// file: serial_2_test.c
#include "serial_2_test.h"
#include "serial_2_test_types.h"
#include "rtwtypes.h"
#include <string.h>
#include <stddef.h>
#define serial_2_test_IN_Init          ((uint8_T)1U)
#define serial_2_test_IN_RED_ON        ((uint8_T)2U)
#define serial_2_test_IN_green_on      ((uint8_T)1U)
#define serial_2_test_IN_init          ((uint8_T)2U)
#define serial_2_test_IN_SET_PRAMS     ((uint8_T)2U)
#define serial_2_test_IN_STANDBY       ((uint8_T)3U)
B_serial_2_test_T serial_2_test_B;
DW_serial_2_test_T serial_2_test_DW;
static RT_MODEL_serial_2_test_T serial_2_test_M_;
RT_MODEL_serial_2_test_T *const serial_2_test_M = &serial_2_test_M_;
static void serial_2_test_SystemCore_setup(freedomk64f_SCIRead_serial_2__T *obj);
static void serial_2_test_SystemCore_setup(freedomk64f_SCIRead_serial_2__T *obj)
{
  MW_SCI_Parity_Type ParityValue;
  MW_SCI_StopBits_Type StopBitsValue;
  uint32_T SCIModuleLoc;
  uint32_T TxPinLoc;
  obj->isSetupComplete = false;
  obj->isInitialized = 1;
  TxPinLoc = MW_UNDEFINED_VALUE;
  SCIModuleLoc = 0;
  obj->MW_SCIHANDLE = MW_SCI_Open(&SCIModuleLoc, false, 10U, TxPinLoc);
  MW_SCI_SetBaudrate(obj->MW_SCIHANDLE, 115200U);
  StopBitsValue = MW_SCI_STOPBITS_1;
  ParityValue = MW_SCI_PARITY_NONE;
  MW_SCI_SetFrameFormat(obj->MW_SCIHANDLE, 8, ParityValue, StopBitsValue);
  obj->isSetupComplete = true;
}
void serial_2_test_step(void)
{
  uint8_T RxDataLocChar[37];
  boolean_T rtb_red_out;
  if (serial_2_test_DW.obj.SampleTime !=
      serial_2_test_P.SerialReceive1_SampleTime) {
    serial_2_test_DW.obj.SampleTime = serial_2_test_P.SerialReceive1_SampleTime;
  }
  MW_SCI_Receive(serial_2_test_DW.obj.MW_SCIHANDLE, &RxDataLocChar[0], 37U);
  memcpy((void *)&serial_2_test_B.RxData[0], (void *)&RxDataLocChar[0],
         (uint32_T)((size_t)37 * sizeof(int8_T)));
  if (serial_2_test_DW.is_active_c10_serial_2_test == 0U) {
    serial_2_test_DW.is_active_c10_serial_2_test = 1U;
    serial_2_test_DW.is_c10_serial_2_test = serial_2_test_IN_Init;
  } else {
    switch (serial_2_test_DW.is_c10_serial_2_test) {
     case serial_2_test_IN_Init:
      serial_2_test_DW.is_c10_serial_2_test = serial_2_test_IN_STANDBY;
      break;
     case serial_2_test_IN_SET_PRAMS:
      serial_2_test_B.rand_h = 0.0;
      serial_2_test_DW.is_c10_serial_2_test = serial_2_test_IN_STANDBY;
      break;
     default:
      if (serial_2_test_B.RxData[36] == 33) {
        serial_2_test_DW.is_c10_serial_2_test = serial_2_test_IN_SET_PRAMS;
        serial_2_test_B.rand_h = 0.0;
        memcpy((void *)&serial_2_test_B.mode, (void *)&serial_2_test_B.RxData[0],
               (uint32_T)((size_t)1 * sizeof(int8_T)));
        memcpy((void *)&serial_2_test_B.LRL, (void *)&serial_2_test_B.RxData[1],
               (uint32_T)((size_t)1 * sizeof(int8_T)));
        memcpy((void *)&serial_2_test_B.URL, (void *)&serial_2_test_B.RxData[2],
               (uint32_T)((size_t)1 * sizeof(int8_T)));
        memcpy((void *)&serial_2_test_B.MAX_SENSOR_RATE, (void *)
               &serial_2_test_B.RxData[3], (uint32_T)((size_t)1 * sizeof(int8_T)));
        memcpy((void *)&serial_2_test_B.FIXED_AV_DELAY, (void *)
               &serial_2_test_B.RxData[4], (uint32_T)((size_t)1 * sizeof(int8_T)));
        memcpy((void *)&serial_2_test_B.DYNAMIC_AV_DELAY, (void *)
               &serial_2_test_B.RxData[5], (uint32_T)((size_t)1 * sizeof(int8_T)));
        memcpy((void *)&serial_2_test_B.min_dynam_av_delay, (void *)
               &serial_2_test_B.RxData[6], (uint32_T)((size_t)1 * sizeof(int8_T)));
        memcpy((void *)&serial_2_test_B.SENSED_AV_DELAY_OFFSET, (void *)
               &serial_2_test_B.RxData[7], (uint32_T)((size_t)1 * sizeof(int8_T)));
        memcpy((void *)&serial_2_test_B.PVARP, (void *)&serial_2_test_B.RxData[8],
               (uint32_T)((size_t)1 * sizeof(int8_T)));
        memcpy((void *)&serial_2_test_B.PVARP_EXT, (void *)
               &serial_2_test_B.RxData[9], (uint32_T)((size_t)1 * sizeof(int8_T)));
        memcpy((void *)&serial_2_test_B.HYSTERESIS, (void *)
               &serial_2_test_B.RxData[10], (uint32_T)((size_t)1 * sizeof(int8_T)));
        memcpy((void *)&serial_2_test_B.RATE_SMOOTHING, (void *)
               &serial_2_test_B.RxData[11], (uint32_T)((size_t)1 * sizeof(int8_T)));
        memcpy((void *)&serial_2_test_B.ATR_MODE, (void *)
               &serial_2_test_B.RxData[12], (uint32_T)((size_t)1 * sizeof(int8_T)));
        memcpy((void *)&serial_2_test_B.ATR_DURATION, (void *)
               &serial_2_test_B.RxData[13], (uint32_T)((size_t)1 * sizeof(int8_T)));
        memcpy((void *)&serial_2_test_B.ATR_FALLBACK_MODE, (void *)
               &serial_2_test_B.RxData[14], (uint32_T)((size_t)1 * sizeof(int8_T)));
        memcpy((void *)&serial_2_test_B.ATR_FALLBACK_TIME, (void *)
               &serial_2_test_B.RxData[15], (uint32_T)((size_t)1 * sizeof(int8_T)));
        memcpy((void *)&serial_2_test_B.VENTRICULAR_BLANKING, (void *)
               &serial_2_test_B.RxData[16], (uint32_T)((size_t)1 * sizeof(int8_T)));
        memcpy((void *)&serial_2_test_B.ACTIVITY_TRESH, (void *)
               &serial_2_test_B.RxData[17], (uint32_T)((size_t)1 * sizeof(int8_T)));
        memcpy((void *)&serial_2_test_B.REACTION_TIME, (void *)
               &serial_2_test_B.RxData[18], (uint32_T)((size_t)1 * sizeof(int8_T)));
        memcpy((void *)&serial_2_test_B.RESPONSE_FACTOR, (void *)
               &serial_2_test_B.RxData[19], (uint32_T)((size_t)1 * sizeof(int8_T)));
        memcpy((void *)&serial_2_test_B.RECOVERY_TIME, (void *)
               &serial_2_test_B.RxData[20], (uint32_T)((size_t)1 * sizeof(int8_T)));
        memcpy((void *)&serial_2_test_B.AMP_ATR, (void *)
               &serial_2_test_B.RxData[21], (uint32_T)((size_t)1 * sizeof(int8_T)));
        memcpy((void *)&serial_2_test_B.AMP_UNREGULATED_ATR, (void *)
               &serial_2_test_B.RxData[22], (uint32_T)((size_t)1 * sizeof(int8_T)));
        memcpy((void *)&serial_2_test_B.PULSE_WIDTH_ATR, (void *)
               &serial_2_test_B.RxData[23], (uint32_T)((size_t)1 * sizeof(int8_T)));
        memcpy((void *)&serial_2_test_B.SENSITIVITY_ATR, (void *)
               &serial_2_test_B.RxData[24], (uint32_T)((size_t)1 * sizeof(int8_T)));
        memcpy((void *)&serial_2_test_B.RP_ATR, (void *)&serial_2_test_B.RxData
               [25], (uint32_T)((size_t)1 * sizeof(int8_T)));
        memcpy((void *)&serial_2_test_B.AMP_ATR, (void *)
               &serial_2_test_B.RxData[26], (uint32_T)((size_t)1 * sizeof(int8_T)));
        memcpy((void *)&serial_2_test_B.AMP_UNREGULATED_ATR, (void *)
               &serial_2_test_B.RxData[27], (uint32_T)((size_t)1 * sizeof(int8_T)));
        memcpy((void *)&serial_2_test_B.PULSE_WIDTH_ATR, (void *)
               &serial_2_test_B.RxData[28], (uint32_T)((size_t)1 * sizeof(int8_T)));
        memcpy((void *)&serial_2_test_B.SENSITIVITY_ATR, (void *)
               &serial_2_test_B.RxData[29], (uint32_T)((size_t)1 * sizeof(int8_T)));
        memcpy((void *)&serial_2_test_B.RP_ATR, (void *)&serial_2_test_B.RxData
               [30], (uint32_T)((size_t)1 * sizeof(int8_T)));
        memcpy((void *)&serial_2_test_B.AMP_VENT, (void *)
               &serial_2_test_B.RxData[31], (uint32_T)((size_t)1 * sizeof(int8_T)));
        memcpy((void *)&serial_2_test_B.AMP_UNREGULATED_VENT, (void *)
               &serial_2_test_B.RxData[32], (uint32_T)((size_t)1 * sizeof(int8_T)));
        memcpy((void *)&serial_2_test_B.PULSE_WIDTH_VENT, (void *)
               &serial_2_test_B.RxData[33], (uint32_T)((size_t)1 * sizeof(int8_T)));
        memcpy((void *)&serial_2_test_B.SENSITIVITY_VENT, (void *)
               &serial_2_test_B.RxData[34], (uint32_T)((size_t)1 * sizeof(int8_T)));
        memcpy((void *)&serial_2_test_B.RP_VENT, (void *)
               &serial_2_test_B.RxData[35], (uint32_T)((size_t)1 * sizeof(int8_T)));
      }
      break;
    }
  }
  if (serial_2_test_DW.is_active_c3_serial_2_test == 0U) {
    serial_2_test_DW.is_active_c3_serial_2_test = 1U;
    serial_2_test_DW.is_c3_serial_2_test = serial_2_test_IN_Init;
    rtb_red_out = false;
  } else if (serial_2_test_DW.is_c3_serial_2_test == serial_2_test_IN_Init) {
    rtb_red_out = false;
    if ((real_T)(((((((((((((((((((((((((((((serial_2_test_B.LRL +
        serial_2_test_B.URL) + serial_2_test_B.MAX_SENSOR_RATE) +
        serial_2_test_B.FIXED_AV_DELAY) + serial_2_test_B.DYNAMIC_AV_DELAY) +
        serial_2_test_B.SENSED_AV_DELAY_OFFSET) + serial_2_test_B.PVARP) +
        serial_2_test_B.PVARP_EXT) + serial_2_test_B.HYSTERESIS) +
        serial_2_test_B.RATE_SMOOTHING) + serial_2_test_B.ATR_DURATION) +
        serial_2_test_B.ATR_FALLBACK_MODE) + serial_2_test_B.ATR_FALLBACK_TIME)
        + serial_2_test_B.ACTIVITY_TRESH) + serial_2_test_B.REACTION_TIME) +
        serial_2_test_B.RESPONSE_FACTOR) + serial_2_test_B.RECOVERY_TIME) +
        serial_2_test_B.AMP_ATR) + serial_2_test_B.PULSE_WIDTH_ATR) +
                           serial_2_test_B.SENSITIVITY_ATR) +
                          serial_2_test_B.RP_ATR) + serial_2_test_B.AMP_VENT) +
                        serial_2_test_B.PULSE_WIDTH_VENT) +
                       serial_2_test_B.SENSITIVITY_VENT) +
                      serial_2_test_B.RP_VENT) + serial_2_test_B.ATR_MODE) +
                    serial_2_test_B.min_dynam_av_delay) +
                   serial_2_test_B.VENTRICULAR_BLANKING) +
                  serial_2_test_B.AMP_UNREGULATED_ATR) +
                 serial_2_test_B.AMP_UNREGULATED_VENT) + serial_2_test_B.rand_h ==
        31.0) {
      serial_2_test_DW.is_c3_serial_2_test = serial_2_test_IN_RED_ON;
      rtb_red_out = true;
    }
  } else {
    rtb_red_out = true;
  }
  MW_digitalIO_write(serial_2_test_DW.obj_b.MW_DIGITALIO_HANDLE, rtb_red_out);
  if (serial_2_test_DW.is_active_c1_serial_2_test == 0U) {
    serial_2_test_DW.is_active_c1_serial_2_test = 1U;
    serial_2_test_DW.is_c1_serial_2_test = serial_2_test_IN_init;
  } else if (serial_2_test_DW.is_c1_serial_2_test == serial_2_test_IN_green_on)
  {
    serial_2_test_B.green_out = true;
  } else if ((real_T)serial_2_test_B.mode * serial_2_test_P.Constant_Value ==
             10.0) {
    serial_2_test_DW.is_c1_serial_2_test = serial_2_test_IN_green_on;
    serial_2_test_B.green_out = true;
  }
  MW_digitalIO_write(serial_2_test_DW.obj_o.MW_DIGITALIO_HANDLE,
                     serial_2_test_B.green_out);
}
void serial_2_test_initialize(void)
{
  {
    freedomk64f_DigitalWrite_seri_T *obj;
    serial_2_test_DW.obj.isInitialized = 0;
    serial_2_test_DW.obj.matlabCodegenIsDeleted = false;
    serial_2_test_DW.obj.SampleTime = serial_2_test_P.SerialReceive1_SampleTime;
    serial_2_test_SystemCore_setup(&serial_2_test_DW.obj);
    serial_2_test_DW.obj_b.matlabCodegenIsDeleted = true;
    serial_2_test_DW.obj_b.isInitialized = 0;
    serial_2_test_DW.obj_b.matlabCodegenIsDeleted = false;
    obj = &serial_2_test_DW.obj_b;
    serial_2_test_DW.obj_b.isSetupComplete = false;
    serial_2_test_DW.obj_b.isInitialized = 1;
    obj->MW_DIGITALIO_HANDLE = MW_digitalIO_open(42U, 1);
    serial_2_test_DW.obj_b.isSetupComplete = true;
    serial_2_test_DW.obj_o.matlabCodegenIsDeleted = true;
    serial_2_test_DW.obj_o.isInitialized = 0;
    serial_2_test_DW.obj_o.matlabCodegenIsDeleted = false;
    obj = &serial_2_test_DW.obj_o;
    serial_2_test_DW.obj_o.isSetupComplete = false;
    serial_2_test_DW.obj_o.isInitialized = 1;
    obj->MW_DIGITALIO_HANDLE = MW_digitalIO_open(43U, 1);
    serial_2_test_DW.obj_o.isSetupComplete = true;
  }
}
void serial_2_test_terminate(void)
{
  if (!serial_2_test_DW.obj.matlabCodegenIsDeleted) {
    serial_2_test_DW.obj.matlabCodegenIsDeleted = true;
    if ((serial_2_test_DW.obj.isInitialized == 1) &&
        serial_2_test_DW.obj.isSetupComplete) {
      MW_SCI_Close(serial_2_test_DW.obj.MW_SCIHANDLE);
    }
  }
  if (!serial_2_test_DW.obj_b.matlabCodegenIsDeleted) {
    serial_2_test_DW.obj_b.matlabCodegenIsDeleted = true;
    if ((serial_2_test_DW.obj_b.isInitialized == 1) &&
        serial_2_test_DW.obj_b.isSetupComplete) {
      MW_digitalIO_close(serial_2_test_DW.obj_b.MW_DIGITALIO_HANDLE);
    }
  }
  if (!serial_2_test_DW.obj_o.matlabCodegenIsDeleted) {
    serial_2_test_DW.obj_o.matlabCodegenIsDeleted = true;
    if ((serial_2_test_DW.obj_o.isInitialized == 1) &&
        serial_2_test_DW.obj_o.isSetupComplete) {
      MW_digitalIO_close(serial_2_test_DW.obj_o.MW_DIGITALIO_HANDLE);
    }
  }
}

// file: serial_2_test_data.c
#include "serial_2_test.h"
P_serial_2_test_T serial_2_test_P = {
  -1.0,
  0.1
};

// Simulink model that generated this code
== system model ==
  DigitalWrite : frdmk64flib/Digital Write  <- 1: Stateflowchart#1
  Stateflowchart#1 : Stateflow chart  <- 1: Sum#1
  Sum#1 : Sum  Inputs=++++++++++++++++++++++++++++++++  <- 1: Stateflowchart#2, 2: Stateflowchart#2/2, 3: Stateflowchart#2/3, 4: Stateflowchart#2/4, 5: Stateflowchart#2/5, 6: Stateflowchart#2/6, 7: Stateflowchart#2/7, 8: Stateflowchart#2/8, 9: Stateflowchart#2/9, 10: Stateflowchart#2/10, 11: Stateflowchart#2/11, 12: Stateflowchart#2/12, 13: Stateflowchart#2/13, 14: Stateflowchart#2/14, 15: Stateflowchart#2/15, 16: Stateflowchart#2/16, 17: Stateflowchart#2/17, 18: Stateflowchart#2/18, 19: Stateflowchart#2/19, 20: Stateflowchart#2/20, 21: Stateflowchart#2/21, 22: Stateflowchart#2/22, 23: Stateflowchart#2/23, 24: Stateflowchart#2/24, 25: Stateflowchart#2/25, 26: Stateflowchart#2/26, 27: Stateflowchart#2/27, 28: Stateflowchart#2/28, 29: Stateflowchart#2/29, 30: Stateflowchart#2/30, 31: Stateflowchart#2/31
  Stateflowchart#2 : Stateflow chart  <- 1: SerialReceive1
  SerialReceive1 : frdmk64flib/Serial Receive
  DigitalWrite#1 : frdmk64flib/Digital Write  <- 1: Stateflowchart#3
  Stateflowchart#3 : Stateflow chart  <- 1: Product#1
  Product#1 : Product  <- 1: Stateflowchart#2/32, 2: Constant
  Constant : Constant  Value=1/10
== stateflow chart Stateflowchart#2 ==
  state SET_PRAMS
    entry:
    rand = 0;
    mode = typecast(rxdata(1),'int8');
    LRL =  typecast(rxdata(2),'int8');
    URL = typecast(rxdata(3),'int8');
    MAX_SENSOR_RATE =  typecast(rxdata(4),'int8');
    FIXED_AV_DELAY =  typecast(rxdata(5),'int8');
    DYNAMIC_AV_DELAY =  typecast(rxdata(6),'int8');
    min_dynam_av_delay = typecast(rxdata(7),'int8');
    SENSED_AV_DELAY_OFFSET =typecast(rxdata(8),'int8');
    PVARP = typecast(rxdata(9),'int8');
    PVARP_EXT = typecast(rxdata(10),'int8');
    HYSTERESIS = typecast(rxdata(11),'int8');
    RATE_SMOOTHING = typecast(rxdata(12),'int8');
    ATR_MODE = typecast(rxdata(13),'int8');
    ATR_DURATION = typecast(rxdata(14),'int8');
    ATR_FALLBACK_MODE =typecast(rxdata(15),'int8');
    ATR_FALLBACK_TIME = typecast(rxdata(16),'int8');
    VENTRICULAR_BLANKING =typecast(rxdata(17),'int8');
    ACTIVITY_TRESH =typecast(rxdata(18),'int8');
    REACTION_TIME = typecast(rxdata(19),'int8');
    RESPONSE_FACTOR =typecast(rxdata(20),'int8');
    RECOVERY_TIME = typecast(rxdata(21),'int8');
    AMP_ATR =typecast(rxdata(22),'int8');
    AMP_UNREGULATED_ATR =typecast(rxdata(23),'int8');
    PULSE_WIDTH_ATR=typecast(rxdata(24),'int8');
    SENSITIVITY_ATR =typecast(rxdata(25),'int8');
    RP_ATR = typecast(rxdata(26),'int8');
    AMP_ATR =typecast(rxdata(27),'int8');
    AMP_UNREGULATED_ATR =typecast(rxdata(28),'int8');
    PULSE_WIDTH_ATR=typecast(rxdata(29),'int8');
    SENSITIVITY_ATR =typecast(rxdata(30),'int8');
    RP_ATR = typecast(rxdata(31),'int8');
    AMP_VENT =typecast(rxdata(32),'int8');
    AMP_UNREGULATED_VENT =typecast(rxdata(33),'int8');
    PULSE_WIDTH_VENT=typecast(rxdata(34),'int8');
    SENSITIVITY_VENT = typecast(rxdata(35),'int8');
    RP_VENT =typecast(rxdata(36),'int8');
  state Init
    entry:
  state STANDBY
  (default) -> Init
  Init -> STANDBY
  STANDBY -> SET_PRAMS : [rxdata(37) == hex2dec('21')]
  SET_PRAMS -> STANDBY
  data: rxdata input; LRL output size=1; URL output size=1; MAX_SENSOR_RATE output size=1; FIXED_AV_DELAY output size=1; DYNAMIC_AV_DELAY output size=1; SENSED_AV_DELAY_OFFSET output size=1; PVARP output size=1; PVARP_EXT output size=1; HYSTERESIS output size=1; RATE_SMOOTHING output size=1; ATR_DURATION output size=1; ATR_FALLBACK_MODE output size=1; ATR_FALLBACK_TIME output size=1; ACTIVITY_TRESH output size=1; REACTION_TIME output size=1; RESPONSE_FACTOR output size=1; RECOVERY_TIME output size=1; AMP_ATR output size=1; PULSE_WIDTH_ATR output size=1; SENSITIVITY_ATR output size=1; RP_ATR output size=1; AMP_VENT output size=1; PULSE_WIDTH_VENT output size=1; SENSITIVITY_VENT output size=1; RP_VENT output size=1; ATR_MODE output size=1; min_dynam_av_delay output size=1; VENTRICULAR_BLANKING output size=1; AMP_UNREGULATED_ATR output size=1; AMP_UNREGULATED_VENT output size=1; rand output size=1; mode output size=1

== stateflow chart Stateflowchart#3 ==
  state green_on
    entry:
    green_out = true;
  state init
    entry:
  (default) -> init
  init -> green_on : [green_en == 10]
  data: green_en input; green_out output

== stateflow chart Stateflowchart#1 ==
  state Init
    entry:
    red_out = false;
  state RED_ON
    entry:
    red_out= true;
  (default) -> Init
  Init -> RED_ON : [data == 31]
  data: data input; red_out output
